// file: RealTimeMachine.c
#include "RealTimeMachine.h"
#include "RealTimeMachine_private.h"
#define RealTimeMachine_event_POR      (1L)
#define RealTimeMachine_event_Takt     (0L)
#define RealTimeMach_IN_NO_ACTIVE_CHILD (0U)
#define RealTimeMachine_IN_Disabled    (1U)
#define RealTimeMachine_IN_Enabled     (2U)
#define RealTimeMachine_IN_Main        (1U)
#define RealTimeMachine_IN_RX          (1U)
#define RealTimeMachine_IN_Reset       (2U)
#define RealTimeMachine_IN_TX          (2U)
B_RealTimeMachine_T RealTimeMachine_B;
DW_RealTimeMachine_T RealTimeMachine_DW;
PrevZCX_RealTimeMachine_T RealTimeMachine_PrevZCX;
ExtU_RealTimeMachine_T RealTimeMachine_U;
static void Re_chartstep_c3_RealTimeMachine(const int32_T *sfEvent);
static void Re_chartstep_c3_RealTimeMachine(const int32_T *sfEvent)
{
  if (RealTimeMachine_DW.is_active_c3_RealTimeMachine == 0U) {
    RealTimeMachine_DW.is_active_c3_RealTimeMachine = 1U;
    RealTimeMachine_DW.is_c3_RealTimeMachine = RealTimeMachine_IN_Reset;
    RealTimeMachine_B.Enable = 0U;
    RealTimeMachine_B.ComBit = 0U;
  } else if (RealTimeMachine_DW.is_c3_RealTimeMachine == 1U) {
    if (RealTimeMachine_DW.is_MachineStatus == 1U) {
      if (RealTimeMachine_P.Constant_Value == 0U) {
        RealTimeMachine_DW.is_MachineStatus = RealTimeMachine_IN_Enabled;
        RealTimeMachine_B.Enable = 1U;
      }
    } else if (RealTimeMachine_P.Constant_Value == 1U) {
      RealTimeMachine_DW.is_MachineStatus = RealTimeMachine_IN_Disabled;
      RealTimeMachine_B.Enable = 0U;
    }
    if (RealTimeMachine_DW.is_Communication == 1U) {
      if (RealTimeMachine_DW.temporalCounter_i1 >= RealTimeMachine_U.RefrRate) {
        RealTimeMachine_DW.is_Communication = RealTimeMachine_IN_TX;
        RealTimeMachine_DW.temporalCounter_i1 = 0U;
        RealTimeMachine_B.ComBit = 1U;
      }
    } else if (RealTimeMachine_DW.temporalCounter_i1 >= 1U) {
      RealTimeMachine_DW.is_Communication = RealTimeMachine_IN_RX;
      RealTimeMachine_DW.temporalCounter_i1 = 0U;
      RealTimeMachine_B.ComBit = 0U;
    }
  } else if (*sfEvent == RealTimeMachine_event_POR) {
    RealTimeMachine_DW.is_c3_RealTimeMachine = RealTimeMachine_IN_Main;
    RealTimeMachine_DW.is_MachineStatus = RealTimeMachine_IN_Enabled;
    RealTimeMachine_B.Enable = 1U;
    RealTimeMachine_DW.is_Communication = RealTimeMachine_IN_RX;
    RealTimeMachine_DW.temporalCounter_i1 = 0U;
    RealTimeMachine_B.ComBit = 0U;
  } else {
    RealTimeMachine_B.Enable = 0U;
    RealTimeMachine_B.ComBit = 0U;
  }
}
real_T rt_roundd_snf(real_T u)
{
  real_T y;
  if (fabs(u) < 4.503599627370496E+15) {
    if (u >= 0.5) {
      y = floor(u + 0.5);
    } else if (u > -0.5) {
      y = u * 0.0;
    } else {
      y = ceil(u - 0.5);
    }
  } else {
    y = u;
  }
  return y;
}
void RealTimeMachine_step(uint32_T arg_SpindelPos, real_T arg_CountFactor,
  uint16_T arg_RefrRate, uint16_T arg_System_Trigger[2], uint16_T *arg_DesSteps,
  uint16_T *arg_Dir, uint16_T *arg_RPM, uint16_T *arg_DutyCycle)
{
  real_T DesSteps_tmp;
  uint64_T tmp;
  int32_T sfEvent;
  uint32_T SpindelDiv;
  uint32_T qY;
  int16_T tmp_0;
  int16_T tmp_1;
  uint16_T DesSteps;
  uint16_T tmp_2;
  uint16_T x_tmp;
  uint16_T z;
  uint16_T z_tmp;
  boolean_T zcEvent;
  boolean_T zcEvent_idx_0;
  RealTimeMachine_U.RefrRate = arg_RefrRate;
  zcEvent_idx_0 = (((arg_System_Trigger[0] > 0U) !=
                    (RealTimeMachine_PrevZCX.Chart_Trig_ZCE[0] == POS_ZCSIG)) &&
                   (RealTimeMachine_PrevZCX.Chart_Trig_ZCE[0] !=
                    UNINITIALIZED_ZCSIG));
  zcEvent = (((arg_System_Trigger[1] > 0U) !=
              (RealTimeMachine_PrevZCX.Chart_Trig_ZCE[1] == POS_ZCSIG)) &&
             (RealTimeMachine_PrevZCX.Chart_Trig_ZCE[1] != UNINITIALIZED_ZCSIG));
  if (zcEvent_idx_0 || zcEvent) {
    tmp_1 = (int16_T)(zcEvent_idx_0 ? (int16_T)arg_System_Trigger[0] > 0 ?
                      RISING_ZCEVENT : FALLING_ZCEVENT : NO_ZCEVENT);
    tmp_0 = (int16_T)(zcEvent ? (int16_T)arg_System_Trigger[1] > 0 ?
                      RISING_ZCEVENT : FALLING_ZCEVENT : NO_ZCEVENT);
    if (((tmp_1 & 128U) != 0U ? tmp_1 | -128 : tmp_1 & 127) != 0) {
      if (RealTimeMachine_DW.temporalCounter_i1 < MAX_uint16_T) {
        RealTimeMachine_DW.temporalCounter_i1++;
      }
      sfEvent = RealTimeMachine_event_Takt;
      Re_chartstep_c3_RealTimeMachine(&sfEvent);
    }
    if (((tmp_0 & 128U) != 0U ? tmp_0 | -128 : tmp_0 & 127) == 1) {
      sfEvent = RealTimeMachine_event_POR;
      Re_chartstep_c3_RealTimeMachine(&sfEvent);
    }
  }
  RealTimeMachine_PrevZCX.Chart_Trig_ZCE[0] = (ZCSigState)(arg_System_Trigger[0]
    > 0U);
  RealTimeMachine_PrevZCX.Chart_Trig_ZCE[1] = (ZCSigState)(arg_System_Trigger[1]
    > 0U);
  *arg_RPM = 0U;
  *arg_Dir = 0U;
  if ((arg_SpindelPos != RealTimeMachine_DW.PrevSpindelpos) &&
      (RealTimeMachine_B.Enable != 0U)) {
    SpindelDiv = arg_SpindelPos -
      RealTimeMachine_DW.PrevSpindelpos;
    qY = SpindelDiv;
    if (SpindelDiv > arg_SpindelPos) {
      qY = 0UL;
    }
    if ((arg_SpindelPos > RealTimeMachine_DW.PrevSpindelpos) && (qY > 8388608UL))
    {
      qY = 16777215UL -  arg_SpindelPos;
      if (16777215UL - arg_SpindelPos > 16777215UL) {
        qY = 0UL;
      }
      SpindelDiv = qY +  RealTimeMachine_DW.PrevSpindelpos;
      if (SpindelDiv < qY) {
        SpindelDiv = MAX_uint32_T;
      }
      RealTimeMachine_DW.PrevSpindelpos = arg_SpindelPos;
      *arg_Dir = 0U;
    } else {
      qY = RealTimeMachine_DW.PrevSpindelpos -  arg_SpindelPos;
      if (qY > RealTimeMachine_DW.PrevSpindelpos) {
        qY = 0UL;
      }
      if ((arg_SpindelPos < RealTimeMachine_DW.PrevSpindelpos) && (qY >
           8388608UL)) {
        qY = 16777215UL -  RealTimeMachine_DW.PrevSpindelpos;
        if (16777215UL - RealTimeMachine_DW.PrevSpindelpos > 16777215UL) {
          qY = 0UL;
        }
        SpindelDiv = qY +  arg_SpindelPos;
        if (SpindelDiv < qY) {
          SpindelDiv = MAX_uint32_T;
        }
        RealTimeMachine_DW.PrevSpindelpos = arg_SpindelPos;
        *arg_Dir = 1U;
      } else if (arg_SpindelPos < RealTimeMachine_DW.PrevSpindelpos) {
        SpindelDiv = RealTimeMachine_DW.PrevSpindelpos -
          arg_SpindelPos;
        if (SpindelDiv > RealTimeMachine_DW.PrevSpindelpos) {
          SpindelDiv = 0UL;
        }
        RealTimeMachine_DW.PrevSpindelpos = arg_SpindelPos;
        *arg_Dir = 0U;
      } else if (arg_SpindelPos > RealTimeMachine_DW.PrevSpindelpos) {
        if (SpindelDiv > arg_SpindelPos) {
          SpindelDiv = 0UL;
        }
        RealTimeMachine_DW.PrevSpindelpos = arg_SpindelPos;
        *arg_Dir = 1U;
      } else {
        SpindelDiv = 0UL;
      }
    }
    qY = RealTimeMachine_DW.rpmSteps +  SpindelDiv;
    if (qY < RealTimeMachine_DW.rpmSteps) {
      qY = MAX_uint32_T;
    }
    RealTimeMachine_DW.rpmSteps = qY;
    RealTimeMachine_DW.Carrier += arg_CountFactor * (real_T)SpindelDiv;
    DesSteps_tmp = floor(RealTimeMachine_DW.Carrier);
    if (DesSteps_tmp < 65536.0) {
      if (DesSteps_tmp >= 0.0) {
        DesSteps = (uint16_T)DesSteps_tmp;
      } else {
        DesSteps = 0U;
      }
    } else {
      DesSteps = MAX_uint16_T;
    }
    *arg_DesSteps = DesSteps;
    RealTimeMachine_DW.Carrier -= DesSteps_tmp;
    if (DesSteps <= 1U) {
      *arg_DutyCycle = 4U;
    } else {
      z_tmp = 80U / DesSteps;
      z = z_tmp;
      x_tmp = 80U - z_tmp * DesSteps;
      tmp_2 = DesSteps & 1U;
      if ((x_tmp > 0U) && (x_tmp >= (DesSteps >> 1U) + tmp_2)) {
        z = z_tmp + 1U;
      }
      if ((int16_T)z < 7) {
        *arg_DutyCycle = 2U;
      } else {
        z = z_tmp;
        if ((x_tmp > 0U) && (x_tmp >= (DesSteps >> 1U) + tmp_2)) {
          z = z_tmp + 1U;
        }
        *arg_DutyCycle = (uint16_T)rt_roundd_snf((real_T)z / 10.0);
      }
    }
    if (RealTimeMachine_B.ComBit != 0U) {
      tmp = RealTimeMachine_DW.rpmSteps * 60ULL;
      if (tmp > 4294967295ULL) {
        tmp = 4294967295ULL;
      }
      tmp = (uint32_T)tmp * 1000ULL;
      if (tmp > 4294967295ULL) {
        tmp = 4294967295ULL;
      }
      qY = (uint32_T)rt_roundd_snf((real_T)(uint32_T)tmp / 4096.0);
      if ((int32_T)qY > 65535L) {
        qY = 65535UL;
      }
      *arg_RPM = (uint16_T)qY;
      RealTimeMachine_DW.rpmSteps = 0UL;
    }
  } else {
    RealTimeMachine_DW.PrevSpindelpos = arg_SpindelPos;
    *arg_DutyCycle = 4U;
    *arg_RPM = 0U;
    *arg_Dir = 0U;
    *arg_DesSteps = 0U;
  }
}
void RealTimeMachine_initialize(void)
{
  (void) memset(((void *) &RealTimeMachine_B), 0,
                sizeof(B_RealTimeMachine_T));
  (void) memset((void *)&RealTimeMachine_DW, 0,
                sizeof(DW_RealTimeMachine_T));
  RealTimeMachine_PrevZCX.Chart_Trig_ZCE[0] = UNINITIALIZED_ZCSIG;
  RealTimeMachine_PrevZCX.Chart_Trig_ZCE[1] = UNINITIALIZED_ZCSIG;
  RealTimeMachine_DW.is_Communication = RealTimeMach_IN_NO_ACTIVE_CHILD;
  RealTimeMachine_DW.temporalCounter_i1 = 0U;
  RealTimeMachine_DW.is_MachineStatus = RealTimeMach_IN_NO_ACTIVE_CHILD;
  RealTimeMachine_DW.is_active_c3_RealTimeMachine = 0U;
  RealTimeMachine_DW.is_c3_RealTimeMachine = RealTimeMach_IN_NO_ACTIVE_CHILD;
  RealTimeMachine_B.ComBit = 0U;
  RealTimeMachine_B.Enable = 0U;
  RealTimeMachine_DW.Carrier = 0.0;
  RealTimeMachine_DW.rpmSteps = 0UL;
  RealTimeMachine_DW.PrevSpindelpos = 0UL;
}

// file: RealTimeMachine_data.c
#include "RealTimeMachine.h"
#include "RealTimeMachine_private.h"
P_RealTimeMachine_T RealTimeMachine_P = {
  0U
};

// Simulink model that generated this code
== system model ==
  SpindelPos : Inport
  CountFactor : Inport
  RefrRate : Inport
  System_Trigger : Inport
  DesSteps : Outport  <- 1: MATLABFunction#1
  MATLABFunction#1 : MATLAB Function  <- 1: Chart, 2: SpindelPos, 3: CountFactor, 4: Chart/2
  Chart : Stateflow chart  <- 1: RefrRate, 2: Constant, Trigger: System_Trigger
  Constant : Constant  Value=0
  Dir : Outport  <- 1: MATLABFunction#1/2
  RPM : Outport  <- 1: MATLABFunction#1/3
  DutyCycle : Outport  <- 1: MATLABFunction#1/4
== matlab function MATLABFunction#1 ==
function [DesSteps, Dir, RPM, DutyCycle] = fcn(ComBit, SpindelPos, Multiplier, Enable)

% Initialization of Variables and Outputs
RPM = uint16(0);
DutyCycle = uint16(130);
Dir = uint16(0);
DesSteps = uint16(0);

%% Declaration of constants
TotalStepTime = uint16(80); %Total time a pulse train is allowed to take in us
rpmRefreshRate = uint16(1000); %RPM calculation Frequency
SingleStepDC = uint16(4); %Single Step Dutycycle in 3us clock cycles (x*3us high, x*3us low)
MaxPos = 0x00FFFFFF; %Point on which the encoder register will overflow 

%% Declaration of persistant variables
persistent Carrier
persistent rpmSteps
persistent PrevSpindelpos

if isempty(Carrier)
    Carrier = 0;
end 

if isempty(rpmSteps)
    rpmSteps = uint32(0);
end

if isempty(PrevSpindelpos)
    PrevSpindelpos = uint32(0);
end

if (SpindelPos ~= PrevSpindelpos) && Enable
    % Spindel in motion
    %% Deal with encoder over/underflow and determine direction
    
    if (SpindelPos > PrevSpindelpos) && ((SpindelPos - PrevSpindelpos) > (MaxPos/2))
        SpindelDiv = (MaxPos - SpindelPos) + PrevSpindelpos;
        PrevSpindelpos = SpindelPos;
        Dir = uint16(0);
        
    elseif(SpindelPos < PrevSpindelpos) && ((PrevSpindelpos - SpindelPos) > (MaxPos/2))
        SpindelDiv = (MaxPos - PrevSpindelpos) + SpindelPos;
        PrevSpindelpos = SpindelPos;
        Dir = uint16(1);
        
    elseif(SpindelPos < PrevSpindelpos)
        SpindelDiv = (PrevSpindelpos - SpindelPos);
        PrevSpindelpos = SpindelPos;
        Dir = uint16(0);
        
    elseif(SpindelPos > PrevSpindelpos)
        SpindelDiv = SpindelPos - PrevSpindelpos;
        PrevSpindelpos = SpindelPos;
        Dir = uint16(1);
    else
        SpindelDiv = uint32(0);
    end

    %% Calculate Desired Steps
    rpmSteps = rpmSteps + uint32(SpindelDiv);
    Carrier = Carrier + (Multiplier * double(SpindelDiv));
    DesSteps = uint16(floor(Carrier));
    Carrier = Carrier - floor(Carrier);

    %% Calculate Dutycycle
    if DesSteps <= 1
        DutyCycle = uint16(SingleStepDC);
    elseif (TotalStepTime/DesSteps) < 7
        DutyCycle = uint16(2);
    else
        DutyCycle = uint16(((TotalStepTime/DesSteps)/10));
    end
            

    %% Calculate current RPM
    if ComBit
        RPM = uint16((rpmSteps*60*uint32(rpmRefreshRate))/4096);
        rpmSteps = uint32(0);
    end

else
    %% Spindel not moving
    PrevSpindelpos = SpindelPos;
    DutyCycle = uint16(SingleStepDC);
    RPM = uint16(0);
    Dir = uint16(0);
    DesSteps = uint16(0);
end
end

== stateflow chart Chart ==
  state Reset
    Enable = 0;
    ComBit = 0;
  state Main
    state MachineStatus [parallel]
      settings: executionOrder=1
      state Enabled
        en: Enable = 1;
      state Disabled
        en: Enable = 0;
      (default) -> Enabled
      Enabled -> Disabled : [Disable == 1]
      Disabled -> Enabled : [Disable == 0]
    state Communication [parallel]
      settings: executionOrder=2
      state RX
        en: ComBit = 0;
      state TX
        en: ComBit = 1;
      (default) -> RX
      TX -> RX : [after(2,Takt)]
      RX -> TX : [after(RefreshRate,Takt)]
  (default) -> Reset
  Reset -> Main : POR
  data: ComBit output uint16; Enable output uint16; RefreshRate input uint16; Disable input uint16
  events: Takt input EITHER_EDGE_EVENT; POR input RISING_EDGE_EVENT
